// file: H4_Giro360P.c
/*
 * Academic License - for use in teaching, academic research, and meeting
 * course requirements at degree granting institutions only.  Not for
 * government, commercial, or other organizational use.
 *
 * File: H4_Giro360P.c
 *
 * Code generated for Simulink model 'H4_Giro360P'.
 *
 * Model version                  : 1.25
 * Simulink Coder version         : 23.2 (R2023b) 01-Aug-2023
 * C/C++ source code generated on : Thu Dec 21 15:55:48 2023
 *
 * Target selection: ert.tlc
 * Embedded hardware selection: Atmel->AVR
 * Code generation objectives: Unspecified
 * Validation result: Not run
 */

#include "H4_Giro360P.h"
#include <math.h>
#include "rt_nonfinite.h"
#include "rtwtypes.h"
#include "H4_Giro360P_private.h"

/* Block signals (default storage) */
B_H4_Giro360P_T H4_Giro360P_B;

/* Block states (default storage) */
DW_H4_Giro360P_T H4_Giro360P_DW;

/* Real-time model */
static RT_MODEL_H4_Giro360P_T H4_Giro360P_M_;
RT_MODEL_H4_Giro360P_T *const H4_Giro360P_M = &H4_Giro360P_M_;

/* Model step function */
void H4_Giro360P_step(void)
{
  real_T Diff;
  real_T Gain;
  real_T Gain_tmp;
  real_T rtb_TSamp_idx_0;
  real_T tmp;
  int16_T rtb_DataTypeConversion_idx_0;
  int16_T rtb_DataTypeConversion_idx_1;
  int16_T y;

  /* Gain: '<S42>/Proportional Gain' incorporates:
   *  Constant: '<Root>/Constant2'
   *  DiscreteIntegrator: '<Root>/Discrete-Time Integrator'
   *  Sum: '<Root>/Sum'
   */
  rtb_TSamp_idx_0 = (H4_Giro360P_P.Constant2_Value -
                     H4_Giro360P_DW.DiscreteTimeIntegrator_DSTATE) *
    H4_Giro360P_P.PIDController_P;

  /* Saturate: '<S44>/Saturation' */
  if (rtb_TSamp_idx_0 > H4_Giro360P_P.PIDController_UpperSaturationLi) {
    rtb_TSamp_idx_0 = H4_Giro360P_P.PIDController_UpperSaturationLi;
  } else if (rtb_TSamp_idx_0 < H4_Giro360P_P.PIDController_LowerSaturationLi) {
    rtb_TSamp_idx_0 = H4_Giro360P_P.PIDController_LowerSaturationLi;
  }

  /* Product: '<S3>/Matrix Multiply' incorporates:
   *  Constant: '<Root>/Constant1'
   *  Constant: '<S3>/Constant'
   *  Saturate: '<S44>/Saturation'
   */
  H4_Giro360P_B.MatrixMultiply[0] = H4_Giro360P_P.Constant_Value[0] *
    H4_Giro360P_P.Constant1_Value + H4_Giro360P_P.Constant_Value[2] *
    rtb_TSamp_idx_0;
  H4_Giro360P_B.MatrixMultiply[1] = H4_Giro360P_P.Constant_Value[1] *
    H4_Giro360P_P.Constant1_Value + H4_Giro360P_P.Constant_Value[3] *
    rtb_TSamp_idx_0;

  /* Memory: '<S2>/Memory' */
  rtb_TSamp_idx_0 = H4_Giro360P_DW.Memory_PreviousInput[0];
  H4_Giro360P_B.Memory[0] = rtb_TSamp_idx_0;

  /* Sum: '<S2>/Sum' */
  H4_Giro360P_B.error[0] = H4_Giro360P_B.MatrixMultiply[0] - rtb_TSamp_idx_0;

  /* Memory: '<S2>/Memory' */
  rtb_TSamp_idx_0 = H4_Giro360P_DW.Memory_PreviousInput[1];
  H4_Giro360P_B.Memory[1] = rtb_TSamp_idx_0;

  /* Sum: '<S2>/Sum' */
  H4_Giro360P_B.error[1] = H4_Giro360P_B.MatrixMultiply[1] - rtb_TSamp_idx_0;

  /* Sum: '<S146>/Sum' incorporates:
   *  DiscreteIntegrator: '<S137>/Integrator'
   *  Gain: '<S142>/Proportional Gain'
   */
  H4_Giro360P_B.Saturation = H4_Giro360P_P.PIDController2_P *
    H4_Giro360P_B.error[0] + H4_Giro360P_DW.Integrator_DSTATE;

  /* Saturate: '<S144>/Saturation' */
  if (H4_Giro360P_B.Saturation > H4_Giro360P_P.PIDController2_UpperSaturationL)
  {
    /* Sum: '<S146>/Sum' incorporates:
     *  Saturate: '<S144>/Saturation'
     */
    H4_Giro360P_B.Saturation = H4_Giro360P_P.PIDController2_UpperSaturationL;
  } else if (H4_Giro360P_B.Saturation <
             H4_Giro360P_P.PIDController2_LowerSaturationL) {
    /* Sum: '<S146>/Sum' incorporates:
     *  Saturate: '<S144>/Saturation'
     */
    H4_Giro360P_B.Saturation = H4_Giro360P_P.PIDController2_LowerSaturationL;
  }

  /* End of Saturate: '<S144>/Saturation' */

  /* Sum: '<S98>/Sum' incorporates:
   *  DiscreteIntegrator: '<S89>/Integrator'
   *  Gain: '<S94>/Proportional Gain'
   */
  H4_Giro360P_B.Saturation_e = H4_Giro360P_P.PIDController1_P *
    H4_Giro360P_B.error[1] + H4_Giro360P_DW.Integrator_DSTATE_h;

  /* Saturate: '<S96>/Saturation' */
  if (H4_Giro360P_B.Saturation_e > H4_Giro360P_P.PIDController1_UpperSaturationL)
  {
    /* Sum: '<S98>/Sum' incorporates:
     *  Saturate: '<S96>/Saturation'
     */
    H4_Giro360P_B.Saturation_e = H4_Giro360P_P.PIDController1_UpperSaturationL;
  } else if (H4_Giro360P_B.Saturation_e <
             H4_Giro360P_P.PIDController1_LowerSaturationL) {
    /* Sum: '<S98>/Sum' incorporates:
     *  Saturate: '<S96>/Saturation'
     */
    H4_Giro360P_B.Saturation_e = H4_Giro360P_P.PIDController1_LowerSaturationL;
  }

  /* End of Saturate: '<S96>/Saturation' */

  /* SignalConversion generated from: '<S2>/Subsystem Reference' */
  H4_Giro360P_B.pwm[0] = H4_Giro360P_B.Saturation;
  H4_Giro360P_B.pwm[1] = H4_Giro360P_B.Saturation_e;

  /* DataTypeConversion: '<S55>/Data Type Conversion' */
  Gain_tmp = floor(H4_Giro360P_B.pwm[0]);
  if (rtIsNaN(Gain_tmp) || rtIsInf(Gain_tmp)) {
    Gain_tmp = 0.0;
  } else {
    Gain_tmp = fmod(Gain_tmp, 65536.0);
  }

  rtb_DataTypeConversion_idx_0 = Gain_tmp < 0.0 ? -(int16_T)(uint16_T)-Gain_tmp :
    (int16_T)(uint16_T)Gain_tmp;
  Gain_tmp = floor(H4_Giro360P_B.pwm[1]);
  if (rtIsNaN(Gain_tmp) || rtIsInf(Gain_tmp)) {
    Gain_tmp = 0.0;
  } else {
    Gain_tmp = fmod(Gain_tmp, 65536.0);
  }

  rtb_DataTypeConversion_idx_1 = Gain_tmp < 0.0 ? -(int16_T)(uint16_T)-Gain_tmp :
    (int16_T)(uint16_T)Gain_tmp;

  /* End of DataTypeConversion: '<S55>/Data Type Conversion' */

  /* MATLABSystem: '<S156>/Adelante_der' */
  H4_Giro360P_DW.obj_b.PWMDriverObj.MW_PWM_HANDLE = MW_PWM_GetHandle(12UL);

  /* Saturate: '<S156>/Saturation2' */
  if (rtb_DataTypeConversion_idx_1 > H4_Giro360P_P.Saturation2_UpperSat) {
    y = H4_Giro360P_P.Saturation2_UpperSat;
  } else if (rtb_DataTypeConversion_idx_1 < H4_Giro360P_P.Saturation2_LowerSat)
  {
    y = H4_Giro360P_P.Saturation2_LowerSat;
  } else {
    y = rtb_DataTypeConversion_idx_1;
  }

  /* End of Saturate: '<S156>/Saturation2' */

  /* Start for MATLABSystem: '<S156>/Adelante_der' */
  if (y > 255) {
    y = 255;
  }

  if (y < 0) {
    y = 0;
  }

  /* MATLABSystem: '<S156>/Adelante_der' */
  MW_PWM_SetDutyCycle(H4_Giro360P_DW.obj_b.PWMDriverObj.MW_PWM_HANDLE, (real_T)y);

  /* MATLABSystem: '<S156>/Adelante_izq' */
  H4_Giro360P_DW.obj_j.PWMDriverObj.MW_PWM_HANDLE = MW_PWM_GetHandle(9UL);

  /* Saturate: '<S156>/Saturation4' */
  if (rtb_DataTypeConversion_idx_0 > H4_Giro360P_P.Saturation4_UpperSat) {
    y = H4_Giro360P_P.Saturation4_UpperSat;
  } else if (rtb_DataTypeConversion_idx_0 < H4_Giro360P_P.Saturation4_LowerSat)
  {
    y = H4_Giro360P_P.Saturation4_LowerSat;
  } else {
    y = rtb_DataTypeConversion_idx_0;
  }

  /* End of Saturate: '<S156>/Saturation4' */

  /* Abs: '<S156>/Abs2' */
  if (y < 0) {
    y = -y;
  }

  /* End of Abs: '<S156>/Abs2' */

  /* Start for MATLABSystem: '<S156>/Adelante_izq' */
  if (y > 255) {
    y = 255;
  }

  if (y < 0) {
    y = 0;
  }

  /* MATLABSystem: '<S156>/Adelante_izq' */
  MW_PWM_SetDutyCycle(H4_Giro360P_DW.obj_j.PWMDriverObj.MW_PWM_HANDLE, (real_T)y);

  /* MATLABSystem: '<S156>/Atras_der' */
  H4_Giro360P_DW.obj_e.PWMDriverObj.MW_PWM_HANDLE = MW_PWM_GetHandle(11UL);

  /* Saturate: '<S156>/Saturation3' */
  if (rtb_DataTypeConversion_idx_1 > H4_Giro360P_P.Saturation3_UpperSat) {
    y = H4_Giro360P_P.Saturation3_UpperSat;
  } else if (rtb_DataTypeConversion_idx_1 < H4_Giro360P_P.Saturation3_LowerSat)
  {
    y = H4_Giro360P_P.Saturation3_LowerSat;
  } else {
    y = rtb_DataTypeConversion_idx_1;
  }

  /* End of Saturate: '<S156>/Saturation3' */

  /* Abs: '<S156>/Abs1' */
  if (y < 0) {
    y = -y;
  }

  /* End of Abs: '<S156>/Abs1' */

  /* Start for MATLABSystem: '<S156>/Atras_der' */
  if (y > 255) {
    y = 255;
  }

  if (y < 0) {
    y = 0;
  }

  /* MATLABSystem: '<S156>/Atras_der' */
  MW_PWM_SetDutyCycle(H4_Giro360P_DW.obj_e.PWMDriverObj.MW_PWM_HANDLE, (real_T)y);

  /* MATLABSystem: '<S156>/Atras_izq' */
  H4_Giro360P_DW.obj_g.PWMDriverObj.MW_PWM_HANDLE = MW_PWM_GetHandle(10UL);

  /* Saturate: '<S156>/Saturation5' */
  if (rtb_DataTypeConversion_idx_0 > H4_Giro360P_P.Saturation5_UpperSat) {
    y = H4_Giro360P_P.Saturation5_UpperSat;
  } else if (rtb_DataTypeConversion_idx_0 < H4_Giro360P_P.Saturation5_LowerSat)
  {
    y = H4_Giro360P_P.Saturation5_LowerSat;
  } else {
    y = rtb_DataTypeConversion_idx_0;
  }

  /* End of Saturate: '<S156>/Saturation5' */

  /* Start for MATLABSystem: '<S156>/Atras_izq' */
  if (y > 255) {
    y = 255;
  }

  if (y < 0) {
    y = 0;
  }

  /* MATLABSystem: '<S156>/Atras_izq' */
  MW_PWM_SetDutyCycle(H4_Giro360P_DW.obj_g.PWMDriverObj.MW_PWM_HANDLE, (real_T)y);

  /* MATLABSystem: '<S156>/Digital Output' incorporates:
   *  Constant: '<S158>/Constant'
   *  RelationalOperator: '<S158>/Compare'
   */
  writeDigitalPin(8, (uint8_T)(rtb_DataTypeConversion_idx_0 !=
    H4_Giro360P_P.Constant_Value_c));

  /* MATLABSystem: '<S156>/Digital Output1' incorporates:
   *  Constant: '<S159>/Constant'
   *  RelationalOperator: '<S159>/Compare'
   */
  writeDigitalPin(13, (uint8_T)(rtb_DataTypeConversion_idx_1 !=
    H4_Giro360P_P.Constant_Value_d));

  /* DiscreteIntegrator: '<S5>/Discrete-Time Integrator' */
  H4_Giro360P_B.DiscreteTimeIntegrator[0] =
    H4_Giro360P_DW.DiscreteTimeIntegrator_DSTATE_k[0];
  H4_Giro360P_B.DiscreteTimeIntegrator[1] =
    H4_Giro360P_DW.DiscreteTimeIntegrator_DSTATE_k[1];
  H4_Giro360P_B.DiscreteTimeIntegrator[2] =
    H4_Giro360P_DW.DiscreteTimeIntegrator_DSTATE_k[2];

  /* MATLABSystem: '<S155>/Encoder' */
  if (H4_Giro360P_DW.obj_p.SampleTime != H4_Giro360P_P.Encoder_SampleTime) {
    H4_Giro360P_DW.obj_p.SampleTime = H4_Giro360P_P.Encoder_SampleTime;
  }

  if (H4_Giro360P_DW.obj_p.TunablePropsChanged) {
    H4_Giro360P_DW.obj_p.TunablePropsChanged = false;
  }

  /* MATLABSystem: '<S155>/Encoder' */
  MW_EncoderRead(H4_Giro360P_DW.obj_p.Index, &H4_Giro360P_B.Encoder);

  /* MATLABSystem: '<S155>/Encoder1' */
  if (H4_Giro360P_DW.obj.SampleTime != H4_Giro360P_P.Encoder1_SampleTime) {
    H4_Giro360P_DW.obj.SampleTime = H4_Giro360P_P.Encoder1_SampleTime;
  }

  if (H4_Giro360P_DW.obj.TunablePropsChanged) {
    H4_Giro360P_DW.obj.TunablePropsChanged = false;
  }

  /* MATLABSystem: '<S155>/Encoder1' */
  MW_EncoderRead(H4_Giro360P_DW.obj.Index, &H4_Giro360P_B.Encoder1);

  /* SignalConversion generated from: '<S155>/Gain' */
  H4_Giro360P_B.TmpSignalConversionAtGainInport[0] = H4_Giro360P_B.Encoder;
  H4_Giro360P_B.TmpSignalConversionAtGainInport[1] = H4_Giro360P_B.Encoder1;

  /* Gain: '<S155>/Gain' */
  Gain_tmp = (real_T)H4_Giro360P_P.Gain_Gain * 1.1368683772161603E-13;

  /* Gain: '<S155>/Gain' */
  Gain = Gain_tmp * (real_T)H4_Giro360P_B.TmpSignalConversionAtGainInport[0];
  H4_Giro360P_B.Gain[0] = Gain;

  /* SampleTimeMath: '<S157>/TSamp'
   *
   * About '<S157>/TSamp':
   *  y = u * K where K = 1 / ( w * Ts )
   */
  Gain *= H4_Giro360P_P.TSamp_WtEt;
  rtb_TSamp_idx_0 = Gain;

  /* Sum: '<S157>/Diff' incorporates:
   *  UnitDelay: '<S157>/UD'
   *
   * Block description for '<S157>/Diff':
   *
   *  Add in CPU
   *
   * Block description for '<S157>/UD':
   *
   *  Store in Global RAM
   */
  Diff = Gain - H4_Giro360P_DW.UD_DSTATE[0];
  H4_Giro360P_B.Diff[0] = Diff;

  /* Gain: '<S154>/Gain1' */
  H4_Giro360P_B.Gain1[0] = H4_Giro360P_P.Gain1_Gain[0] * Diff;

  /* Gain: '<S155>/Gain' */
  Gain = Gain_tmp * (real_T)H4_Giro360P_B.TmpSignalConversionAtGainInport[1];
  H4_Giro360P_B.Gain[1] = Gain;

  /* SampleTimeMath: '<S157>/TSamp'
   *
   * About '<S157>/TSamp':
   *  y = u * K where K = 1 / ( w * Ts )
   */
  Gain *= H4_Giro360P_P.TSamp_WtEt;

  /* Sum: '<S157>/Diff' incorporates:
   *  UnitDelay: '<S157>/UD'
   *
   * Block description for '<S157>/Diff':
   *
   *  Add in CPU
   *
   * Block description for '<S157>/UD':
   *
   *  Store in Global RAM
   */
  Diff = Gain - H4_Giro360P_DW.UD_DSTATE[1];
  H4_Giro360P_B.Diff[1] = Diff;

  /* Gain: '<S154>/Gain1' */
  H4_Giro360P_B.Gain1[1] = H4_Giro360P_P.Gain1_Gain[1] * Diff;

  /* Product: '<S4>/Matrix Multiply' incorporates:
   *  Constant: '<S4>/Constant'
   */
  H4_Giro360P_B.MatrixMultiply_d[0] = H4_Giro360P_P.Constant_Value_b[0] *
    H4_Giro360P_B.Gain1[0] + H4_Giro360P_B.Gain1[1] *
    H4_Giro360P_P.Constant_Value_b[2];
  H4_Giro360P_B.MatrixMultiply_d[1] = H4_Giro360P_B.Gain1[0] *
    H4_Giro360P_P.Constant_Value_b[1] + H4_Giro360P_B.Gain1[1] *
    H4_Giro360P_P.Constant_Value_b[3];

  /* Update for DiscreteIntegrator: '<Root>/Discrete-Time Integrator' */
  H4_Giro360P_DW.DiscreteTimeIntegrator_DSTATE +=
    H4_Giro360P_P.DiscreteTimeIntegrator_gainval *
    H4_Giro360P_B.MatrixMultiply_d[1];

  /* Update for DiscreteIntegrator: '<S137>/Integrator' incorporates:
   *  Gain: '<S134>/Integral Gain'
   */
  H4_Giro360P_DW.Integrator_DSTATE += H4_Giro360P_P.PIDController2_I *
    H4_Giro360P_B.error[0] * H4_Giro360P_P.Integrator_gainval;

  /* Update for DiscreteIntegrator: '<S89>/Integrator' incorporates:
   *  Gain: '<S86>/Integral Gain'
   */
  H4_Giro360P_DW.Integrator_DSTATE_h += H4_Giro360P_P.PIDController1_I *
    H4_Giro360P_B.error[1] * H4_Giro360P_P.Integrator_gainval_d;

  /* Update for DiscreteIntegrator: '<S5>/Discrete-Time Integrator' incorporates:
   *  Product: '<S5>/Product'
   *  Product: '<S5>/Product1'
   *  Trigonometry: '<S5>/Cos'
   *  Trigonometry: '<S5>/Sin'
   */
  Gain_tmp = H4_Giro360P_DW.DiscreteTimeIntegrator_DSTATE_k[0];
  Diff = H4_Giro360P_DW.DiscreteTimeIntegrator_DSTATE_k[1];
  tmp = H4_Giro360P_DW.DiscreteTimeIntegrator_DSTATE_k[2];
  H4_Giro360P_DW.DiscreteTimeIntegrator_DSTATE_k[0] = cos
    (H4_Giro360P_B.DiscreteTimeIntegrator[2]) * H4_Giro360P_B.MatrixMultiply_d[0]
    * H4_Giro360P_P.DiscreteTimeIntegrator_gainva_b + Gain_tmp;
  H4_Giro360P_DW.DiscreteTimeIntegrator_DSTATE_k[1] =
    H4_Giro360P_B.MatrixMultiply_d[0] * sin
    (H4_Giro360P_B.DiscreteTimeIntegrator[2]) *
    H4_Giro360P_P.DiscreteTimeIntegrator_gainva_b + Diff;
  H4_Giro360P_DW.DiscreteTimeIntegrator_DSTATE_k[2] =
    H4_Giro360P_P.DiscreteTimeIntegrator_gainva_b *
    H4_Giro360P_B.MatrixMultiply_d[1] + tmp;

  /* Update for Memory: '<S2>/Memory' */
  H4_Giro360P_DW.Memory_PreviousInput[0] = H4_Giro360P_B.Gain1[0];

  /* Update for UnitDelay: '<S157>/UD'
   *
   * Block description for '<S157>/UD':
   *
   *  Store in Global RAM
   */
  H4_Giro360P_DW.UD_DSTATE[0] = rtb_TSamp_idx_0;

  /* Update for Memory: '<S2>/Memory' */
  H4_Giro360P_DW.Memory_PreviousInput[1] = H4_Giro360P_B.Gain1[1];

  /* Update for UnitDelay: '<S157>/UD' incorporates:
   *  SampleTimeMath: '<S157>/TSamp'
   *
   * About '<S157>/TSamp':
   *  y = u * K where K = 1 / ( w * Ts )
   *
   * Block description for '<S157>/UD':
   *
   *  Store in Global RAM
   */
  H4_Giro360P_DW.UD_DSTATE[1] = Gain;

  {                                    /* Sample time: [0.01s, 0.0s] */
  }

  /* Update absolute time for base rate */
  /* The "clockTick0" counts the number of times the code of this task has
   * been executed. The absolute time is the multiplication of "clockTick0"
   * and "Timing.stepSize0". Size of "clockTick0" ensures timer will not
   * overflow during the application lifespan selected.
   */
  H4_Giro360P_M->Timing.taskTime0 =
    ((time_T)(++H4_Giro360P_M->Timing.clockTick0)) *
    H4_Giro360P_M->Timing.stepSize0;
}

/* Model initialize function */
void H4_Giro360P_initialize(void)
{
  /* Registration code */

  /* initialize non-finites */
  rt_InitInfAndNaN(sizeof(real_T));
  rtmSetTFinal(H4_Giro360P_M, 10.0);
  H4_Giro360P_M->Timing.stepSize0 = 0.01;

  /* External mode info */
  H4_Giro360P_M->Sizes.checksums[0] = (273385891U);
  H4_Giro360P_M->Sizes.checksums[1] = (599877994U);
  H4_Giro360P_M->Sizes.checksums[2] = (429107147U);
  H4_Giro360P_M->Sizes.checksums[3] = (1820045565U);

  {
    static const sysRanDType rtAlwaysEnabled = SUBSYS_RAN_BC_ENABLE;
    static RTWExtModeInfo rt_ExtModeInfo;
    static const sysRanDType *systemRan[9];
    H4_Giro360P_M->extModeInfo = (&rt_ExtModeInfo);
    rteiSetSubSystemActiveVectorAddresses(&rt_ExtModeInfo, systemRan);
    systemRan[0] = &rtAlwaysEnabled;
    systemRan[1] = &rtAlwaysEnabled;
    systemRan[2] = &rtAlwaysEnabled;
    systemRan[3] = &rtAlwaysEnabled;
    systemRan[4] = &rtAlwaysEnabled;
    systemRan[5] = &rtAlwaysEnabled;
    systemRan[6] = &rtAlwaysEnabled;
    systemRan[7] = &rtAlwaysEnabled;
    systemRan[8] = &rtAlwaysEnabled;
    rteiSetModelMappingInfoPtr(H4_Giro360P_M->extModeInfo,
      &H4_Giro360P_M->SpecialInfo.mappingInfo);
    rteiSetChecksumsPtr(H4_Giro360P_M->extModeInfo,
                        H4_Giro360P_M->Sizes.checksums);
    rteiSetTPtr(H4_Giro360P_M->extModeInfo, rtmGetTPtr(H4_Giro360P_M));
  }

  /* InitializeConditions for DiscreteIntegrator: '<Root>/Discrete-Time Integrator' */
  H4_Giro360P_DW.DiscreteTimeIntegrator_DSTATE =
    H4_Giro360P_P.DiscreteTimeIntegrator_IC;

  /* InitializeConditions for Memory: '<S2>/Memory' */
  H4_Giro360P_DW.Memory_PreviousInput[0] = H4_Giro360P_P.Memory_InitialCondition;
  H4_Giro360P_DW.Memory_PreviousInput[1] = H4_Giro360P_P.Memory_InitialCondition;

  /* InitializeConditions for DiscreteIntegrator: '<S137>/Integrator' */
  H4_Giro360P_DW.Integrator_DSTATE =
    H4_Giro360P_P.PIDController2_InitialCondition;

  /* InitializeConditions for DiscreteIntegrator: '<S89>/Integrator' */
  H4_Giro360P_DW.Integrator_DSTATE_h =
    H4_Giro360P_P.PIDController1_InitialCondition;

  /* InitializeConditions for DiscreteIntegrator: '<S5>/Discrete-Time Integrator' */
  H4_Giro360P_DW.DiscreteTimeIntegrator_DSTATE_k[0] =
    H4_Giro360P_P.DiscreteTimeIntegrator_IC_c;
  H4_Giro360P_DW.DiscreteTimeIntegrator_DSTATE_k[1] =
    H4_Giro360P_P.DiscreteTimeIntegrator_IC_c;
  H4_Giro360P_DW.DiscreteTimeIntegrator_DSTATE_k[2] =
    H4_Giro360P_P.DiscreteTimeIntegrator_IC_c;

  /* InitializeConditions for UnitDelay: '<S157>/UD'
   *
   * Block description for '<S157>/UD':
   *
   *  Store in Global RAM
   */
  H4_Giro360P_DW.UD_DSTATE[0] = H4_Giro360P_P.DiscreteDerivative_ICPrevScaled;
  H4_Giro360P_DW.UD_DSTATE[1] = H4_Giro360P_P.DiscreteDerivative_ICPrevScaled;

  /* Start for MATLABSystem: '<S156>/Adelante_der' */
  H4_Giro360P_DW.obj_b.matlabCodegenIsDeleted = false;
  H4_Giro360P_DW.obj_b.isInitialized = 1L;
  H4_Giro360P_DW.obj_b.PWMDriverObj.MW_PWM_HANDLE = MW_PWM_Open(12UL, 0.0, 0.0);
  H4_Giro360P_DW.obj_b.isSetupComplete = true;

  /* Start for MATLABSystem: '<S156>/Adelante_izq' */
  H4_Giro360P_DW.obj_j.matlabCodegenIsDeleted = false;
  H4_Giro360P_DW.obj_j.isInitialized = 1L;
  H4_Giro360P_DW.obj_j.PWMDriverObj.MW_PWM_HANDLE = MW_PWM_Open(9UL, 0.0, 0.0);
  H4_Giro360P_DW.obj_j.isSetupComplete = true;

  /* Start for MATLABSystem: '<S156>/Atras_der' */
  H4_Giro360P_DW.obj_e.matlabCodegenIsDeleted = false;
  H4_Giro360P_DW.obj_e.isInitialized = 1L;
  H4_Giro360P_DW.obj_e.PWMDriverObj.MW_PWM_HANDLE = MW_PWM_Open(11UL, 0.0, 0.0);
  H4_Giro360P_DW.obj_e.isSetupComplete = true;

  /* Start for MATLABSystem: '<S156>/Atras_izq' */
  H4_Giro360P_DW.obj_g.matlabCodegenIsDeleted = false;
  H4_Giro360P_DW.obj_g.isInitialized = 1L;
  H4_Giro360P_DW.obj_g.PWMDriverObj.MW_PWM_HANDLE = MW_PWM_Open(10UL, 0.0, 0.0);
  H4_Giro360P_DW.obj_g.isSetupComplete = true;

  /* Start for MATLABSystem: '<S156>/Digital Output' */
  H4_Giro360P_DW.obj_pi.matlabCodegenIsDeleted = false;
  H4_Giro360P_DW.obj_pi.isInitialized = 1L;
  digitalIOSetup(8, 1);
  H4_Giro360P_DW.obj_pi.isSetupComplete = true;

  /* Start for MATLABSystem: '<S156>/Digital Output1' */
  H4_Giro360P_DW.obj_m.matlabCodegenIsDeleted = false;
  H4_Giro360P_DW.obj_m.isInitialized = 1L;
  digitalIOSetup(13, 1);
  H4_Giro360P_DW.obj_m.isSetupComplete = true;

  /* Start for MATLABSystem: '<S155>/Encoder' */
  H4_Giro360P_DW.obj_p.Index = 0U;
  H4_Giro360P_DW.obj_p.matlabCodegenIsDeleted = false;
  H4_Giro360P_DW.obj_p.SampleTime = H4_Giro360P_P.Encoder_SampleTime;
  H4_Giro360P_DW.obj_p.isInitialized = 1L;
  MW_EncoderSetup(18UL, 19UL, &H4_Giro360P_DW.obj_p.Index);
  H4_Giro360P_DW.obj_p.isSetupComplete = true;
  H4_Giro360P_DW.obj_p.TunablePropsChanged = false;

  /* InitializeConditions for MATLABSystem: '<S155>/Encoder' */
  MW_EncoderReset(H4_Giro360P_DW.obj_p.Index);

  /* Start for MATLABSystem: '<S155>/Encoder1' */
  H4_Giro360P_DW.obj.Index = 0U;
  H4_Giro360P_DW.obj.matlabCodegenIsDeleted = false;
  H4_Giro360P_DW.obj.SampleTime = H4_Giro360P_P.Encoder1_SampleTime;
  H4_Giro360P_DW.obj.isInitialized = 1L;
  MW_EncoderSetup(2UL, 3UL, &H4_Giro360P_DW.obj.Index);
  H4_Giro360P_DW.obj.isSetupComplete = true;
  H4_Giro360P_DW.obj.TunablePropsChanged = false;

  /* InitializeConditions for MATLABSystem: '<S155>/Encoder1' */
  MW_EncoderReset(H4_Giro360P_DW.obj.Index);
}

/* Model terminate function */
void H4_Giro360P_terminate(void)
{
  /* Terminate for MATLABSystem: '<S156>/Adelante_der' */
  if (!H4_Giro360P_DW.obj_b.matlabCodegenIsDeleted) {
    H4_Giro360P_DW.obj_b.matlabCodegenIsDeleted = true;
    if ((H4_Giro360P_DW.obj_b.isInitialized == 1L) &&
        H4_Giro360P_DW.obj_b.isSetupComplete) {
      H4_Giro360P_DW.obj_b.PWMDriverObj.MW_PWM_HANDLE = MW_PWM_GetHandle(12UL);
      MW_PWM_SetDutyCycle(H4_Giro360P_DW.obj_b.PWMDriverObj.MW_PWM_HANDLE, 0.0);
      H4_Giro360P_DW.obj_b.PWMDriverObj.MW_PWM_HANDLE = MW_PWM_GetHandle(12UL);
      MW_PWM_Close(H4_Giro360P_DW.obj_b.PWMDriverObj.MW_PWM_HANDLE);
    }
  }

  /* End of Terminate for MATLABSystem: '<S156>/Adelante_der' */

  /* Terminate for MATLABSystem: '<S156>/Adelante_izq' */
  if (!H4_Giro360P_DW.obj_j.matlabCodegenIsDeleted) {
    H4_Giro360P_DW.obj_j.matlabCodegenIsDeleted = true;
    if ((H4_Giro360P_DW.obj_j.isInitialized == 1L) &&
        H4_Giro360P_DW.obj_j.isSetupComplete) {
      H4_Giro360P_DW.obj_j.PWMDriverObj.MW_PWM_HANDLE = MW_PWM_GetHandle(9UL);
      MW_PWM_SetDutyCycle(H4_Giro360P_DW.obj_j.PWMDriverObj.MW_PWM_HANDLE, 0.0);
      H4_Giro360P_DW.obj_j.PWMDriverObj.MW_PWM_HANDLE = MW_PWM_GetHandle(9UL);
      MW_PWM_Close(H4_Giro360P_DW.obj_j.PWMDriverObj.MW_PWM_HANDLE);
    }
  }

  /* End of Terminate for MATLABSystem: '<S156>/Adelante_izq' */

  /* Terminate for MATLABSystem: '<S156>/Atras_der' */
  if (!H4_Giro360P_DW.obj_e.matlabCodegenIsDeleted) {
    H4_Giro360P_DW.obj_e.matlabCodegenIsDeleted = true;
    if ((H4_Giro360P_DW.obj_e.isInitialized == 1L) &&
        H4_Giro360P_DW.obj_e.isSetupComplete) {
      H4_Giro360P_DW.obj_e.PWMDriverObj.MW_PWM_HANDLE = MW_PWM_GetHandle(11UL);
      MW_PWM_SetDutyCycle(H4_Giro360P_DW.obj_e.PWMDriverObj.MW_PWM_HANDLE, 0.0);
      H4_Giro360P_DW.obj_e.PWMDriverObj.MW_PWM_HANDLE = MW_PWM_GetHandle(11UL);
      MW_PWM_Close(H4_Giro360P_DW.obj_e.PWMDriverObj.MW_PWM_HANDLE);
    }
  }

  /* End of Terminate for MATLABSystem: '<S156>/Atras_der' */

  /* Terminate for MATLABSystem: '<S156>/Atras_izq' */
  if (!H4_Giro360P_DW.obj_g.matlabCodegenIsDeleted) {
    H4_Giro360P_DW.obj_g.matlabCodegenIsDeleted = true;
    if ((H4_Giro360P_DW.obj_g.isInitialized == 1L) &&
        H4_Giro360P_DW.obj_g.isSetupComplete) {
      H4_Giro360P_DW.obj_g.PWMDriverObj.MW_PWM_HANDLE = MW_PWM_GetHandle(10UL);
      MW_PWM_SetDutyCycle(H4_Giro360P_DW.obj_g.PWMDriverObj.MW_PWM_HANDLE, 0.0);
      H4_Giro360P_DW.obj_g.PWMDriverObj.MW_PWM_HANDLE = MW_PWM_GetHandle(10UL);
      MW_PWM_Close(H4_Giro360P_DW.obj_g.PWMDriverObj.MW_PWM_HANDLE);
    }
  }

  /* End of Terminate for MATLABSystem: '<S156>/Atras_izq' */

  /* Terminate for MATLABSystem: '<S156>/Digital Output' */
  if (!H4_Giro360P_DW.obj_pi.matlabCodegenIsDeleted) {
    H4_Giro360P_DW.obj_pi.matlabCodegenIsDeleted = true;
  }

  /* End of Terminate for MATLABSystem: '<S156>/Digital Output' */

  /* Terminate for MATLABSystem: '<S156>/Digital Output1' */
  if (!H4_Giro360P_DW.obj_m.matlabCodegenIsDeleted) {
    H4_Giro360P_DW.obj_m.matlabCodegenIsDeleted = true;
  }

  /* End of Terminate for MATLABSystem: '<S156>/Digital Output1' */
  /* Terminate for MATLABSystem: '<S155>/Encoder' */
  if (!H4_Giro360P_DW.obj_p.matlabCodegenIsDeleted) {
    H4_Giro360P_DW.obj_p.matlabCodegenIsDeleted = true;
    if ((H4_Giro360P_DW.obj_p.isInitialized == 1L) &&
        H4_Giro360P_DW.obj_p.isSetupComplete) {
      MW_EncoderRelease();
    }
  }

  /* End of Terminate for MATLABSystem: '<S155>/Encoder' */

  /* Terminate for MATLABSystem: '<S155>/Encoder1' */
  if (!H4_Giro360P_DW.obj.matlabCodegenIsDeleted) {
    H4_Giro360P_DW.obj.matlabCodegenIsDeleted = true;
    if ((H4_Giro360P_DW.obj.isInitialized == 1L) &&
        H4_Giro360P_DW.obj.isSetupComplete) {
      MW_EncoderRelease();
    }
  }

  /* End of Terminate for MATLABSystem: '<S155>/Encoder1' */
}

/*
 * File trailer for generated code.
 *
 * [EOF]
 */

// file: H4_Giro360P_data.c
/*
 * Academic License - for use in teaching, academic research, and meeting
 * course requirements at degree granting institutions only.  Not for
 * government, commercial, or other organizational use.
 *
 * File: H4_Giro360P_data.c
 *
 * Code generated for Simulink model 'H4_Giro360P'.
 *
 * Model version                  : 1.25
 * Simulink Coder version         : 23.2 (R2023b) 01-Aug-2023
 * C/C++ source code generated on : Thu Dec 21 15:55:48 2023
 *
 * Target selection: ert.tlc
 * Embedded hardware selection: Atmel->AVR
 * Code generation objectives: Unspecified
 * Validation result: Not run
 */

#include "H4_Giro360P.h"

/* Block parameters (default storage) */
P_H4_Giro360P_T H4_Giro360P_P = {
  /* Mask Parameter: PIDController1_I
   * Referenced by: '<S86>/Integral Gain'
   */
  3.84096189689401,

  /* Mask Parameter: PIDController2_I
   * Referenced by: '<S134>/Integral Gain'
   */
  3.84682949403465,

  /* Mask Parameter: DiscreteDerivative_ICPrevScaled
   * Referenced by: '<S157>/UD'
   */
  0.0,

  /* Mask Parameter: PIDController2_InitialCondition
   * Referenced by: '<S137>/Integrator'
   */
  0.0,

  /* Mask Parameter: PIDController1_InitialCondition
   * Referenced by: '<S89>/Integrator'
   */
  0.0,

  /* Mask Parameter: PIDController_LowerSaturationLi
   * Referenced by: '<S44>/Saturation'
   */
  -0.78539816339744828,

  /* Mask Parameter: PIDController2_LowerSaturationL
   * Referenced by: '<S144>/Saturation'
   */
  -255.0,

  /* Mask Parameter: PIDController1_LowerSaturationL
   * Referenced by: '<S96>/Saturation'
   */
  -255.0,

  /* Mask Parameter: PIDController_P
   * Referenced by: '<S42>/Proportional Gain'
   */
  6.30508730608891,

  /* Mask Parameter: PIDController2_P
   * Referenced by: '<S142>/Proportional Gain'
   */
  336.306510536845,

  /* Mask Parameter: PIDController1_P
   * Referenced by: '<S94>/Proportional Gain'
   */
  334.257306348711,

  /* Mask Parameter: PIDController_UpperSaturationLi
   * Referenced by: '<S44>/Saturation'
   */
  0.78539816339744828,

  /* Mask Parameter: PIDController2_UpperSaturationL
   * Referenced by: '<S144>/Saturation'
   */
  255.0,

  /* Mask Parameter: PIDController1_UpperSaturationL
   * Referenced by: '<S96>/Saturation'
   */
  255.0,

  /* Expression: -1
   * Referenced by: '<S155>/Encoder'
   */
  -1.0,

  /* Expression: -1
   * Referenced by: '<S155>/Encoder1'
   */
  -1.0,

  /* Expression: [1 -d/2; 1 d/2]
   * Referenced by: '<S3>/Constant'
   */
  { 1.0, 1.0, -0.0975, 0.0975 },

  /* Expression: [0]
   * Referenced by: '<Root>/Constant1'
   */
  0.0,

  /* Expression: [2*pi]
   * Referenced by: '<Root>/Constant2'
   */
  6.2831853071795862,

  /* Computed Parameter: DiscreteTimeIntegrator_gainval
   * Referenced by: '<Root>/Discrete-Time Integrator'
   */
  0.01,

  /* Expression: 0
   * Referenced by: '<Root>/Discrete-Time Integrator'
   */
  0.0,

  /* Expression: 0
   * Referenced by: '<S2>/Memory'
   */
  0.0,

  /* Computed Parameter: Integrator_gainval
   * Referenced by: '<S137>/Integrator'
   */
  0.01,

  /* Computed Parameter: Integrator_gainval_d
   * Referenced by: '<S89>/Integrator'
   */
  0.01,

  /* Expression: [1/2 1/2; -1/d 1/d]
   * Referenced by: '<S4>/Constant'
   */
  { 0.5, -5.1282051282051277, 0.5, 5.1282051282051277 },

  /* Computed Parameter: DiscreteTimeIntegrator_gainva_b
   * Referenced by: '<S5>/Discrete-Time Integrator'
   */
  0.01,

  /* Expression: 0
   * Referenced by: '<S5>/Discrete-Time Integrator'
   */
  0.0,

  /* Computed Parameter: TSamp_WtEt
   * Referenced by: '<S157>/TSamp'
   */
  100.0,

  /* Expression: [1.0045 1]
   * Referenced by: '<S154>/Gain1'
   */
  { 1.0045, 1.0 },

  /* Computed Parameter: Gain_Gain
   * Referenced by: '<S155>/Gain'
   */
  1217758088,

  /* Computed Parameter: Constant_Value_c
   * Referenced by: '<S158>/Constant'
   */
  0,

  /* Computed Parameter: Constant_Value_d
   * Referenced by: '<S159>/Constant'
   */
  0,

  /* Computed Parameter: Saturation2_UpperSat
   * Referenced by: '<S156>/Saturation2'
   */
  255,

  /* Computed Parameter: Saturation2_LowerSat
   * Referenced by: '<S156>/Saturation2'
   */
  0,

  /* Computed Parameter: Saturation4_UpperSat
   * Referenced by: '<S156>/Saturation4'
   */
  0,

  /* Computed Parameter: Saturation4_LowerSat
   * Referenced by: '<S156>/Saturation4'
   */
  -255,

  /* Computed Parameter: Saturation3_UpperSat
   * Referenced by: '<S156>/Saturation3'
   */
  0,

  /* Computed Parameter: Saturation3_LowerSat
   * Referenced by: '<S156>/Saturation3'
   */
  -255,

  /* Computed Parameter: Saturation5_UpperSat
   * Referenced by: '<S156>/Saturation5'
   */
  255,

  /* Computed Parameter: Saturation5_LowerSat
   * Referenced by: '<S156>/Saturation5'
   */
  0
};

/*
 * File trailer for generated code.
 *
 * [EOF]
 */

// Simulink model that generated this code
simulink model "H4_Giro360P"  (R2023b)
settings: Solver=FixedStepDiscrete  StartTime=0.0  StopTime=10  FixedStep=0.01  RelTol=1e-3  EnableMultiTasking=on
model workspace (MAT data in the model file):
  d = 0.195
undefined symbols (not defined in the file): DiscIntNeverNeededParam
libraries: slpidlib x1

== system H4_Giro360P ==
  Constant1 : Constant  Value=[0]
  Constant2 : Constant  Value=[2*pi]
  Demux : Demux  Outputs=2
  Discrete-Time Integrator : DiscreteIntegrator  SampleTime=-1  ICPrevOutput=DiscIntNeverNeededParam  ICPrevScaledInput=DiscIntNeverNeededParam
  Mux : Mux  Inputs=2
  PID Controller : slpidlib/PID Controller  Controller=P  Form=Parallel  TimeDomain=Discrete-time  UseExternalTs=off  SampleTime=-1  IntegratorMethod=Forward Euler  FilterMethod=Forward Euler  ControllerParametersSource=internal  P=6.30508730608891  I=0.247257832491171  UseKiTs=off  D=0  N=100  UseFilter=on  TunerSelectOption=Transfer Function Based (PID Tuner App)  InitialConditionSource=internal  InitialConditionForIntegrator=0  InitialConditionForFilter=0  DifferentiatorICPrevScaledInput=0  ExternalReset=none  TrackingMode=off  Kt=1  LimitOutput=on  SatLimitsSource=internal  UpperSaturationLimit=2*pi/8  LowerSaturationLimit=-2*pi/8  LinearizeAsGain=on  AntiWindupMode=none  Kb=1  LimitIntegrator=off  UpperIntegratorSaturationLimit=inf  LowerIntegratorSaturationLimit=-inf  POutMin=[]  POutMax=[]  IOutMin=[]  IOutMax=[]  DOutMin=[]  DOutMax=[]  NOutMin=[]  NOutMax=[]  SumOutMin=[]  SumOutMax=[]  SaturationOutMin=[]  SaturationOutMax=[]  PParamMin=[]  PParamMax=[]  IParamMin=[]  IParamMax=[]  DParamMin=[]  DParamMax=[]  NParamMin=[]  NParamMax=[]  KbParamMin=[]  KbParamMax=[]  KtParamMin=[]  KtParamMax=[]  KbOutMin=[]  KbOutMax=[]  KtOutMin=[]  KtOutMax=[]  IntegratorOutMin=[]  IntegratorOutMax=[]  FilterOutMin=[]  FilterOutMax=[]  SumI1OutMin=[]  SumI1OutMax=[]  SumI2OutMin=[]  SumI2OutMax=[]  SumI3OutMin=[]  SumI3OutMax=[]  SumI4OutMin=[]  SumI4OutMax=[]  SumDOutMin=[]  SumDOutMax=[]  DifferentiatorOutMin=[]  DifferentiatorOutMax=[]  FilterDiffOutCoefMin=[]  FilterDiffOutCoefMax=[]  ReciprocalOutMin=[]  ReciprocalOutMax=[]  SumDenOutMin=[]  SumDenOutMax=[]  SumNumOutMin=[]  SumNumOutMax=[]  DivideOutMin=[]  DivideOutMax=[]  UdiffTsProdOutMin=[]  UdiffTsProdOutMax=[]  NTsProdOutMin=[]  NTsProdOutMax=[]  UintegralTsProdOutMin=[]  UintegralTsProdOutMax=[]  UngainTsProdOutMin=[]  UngainTsProdOutMax=[]  ClampingZeroOutDataTypeStr=Inherit: Inherit via back propagation  ClampingZeroOutMin=[]  ClampingZeroOutMax=[]  FilterDenConstantOutDataTypeStr=Inherit: Inherit via back propagation  FilterDenConstantOutMin=[]  FilterDenConstantOutMax=[]  PCopyOutDataTypeStr=Inherit: Inherit via back propagation  PCopyOutMin=[]  PCopyOutMax=[]  NCopyOutDataTypeStr=Inherit: Inherit via back propagation  NCopyOutMin=[]  NCopyOutMax=[]  IntegratorContinuousStateAttributes=''  IntegratorStateMustResolveToSignalObject=off  IntegratorRTWStateStorageClass=Auto  FilterContinuousStateAttributes=''  FilterStateMustResolveToSignalObject=off  FilterRTWStateStorageClass=Auto  ParallelPVariant=InternalParameters  IdealPVariant=Disabled  IVariant=Disabled  DVariant=Disabled  IntegratorVariant=Disabled  SatVariant=Enabled  AWVariant=Disabled  PCopyVariant=Disabled  TRVariant=Disabled  FdbkBlocksVariant=Forward  IdealPFdbkVariant=Disabled  SatFdbkVariant=Disabled  DerivativeFilterVariant=Disabled  NVariant=Disabled  NCopyVariant=Disabled_SignalSpec  FilterICVariant=Disabled  IntegratorICVariant=Disabled  ExternalResetVariant=Disabled  TRSumVariant=Passthrough  SumFdbkVariant=Disabled  SumVariant=Passthrough_P  TsampFilterVariant=InternalTs  TsampNgainVariant=Passthrough  TsampIntegralVariant=Disabled_SignalSpec  ExternalSaturationOutDataTypeStr=Inherit: Same as second input
  Subsystem Reference : Subsystem  ReferencedSubsystem=Piero_ControladoZ_memoria
  Subsystem Reference1 : Subsystem  ReferencedSubsystem=MCI2
  Subsystem Reference2 : Subsystem  ReferencedSubsystem=MCD2
  Subsystem Reference4 : Subsystem  ReferencedSubsystem=OdometriaZ
  Sum : Sum  Inputs=|+-
  Terminator : Terminator
  wires:
  Subsystem Reference1/1 -> Subsystem Reference/1
  Subsystem Reference2/1 -> Demux/1, Subsystem Reference4/1
  Subsystem Reference/1 -> Subsystem Reference2/1
  PID Controller/1 -> Mux/2  "rel"
  Mux/1 -> Subsystem Reference1/1
  Constant1/1 -> Mux/1
  Sum/1 -> PID Controller/1
  Constant2/1 -> Sum/1
  Demux/1 -> Terminator/1
  Demux/2 -> Discrete-Time Integrator/1
  Discrete-Time Integrator/1 -> Sum/2
